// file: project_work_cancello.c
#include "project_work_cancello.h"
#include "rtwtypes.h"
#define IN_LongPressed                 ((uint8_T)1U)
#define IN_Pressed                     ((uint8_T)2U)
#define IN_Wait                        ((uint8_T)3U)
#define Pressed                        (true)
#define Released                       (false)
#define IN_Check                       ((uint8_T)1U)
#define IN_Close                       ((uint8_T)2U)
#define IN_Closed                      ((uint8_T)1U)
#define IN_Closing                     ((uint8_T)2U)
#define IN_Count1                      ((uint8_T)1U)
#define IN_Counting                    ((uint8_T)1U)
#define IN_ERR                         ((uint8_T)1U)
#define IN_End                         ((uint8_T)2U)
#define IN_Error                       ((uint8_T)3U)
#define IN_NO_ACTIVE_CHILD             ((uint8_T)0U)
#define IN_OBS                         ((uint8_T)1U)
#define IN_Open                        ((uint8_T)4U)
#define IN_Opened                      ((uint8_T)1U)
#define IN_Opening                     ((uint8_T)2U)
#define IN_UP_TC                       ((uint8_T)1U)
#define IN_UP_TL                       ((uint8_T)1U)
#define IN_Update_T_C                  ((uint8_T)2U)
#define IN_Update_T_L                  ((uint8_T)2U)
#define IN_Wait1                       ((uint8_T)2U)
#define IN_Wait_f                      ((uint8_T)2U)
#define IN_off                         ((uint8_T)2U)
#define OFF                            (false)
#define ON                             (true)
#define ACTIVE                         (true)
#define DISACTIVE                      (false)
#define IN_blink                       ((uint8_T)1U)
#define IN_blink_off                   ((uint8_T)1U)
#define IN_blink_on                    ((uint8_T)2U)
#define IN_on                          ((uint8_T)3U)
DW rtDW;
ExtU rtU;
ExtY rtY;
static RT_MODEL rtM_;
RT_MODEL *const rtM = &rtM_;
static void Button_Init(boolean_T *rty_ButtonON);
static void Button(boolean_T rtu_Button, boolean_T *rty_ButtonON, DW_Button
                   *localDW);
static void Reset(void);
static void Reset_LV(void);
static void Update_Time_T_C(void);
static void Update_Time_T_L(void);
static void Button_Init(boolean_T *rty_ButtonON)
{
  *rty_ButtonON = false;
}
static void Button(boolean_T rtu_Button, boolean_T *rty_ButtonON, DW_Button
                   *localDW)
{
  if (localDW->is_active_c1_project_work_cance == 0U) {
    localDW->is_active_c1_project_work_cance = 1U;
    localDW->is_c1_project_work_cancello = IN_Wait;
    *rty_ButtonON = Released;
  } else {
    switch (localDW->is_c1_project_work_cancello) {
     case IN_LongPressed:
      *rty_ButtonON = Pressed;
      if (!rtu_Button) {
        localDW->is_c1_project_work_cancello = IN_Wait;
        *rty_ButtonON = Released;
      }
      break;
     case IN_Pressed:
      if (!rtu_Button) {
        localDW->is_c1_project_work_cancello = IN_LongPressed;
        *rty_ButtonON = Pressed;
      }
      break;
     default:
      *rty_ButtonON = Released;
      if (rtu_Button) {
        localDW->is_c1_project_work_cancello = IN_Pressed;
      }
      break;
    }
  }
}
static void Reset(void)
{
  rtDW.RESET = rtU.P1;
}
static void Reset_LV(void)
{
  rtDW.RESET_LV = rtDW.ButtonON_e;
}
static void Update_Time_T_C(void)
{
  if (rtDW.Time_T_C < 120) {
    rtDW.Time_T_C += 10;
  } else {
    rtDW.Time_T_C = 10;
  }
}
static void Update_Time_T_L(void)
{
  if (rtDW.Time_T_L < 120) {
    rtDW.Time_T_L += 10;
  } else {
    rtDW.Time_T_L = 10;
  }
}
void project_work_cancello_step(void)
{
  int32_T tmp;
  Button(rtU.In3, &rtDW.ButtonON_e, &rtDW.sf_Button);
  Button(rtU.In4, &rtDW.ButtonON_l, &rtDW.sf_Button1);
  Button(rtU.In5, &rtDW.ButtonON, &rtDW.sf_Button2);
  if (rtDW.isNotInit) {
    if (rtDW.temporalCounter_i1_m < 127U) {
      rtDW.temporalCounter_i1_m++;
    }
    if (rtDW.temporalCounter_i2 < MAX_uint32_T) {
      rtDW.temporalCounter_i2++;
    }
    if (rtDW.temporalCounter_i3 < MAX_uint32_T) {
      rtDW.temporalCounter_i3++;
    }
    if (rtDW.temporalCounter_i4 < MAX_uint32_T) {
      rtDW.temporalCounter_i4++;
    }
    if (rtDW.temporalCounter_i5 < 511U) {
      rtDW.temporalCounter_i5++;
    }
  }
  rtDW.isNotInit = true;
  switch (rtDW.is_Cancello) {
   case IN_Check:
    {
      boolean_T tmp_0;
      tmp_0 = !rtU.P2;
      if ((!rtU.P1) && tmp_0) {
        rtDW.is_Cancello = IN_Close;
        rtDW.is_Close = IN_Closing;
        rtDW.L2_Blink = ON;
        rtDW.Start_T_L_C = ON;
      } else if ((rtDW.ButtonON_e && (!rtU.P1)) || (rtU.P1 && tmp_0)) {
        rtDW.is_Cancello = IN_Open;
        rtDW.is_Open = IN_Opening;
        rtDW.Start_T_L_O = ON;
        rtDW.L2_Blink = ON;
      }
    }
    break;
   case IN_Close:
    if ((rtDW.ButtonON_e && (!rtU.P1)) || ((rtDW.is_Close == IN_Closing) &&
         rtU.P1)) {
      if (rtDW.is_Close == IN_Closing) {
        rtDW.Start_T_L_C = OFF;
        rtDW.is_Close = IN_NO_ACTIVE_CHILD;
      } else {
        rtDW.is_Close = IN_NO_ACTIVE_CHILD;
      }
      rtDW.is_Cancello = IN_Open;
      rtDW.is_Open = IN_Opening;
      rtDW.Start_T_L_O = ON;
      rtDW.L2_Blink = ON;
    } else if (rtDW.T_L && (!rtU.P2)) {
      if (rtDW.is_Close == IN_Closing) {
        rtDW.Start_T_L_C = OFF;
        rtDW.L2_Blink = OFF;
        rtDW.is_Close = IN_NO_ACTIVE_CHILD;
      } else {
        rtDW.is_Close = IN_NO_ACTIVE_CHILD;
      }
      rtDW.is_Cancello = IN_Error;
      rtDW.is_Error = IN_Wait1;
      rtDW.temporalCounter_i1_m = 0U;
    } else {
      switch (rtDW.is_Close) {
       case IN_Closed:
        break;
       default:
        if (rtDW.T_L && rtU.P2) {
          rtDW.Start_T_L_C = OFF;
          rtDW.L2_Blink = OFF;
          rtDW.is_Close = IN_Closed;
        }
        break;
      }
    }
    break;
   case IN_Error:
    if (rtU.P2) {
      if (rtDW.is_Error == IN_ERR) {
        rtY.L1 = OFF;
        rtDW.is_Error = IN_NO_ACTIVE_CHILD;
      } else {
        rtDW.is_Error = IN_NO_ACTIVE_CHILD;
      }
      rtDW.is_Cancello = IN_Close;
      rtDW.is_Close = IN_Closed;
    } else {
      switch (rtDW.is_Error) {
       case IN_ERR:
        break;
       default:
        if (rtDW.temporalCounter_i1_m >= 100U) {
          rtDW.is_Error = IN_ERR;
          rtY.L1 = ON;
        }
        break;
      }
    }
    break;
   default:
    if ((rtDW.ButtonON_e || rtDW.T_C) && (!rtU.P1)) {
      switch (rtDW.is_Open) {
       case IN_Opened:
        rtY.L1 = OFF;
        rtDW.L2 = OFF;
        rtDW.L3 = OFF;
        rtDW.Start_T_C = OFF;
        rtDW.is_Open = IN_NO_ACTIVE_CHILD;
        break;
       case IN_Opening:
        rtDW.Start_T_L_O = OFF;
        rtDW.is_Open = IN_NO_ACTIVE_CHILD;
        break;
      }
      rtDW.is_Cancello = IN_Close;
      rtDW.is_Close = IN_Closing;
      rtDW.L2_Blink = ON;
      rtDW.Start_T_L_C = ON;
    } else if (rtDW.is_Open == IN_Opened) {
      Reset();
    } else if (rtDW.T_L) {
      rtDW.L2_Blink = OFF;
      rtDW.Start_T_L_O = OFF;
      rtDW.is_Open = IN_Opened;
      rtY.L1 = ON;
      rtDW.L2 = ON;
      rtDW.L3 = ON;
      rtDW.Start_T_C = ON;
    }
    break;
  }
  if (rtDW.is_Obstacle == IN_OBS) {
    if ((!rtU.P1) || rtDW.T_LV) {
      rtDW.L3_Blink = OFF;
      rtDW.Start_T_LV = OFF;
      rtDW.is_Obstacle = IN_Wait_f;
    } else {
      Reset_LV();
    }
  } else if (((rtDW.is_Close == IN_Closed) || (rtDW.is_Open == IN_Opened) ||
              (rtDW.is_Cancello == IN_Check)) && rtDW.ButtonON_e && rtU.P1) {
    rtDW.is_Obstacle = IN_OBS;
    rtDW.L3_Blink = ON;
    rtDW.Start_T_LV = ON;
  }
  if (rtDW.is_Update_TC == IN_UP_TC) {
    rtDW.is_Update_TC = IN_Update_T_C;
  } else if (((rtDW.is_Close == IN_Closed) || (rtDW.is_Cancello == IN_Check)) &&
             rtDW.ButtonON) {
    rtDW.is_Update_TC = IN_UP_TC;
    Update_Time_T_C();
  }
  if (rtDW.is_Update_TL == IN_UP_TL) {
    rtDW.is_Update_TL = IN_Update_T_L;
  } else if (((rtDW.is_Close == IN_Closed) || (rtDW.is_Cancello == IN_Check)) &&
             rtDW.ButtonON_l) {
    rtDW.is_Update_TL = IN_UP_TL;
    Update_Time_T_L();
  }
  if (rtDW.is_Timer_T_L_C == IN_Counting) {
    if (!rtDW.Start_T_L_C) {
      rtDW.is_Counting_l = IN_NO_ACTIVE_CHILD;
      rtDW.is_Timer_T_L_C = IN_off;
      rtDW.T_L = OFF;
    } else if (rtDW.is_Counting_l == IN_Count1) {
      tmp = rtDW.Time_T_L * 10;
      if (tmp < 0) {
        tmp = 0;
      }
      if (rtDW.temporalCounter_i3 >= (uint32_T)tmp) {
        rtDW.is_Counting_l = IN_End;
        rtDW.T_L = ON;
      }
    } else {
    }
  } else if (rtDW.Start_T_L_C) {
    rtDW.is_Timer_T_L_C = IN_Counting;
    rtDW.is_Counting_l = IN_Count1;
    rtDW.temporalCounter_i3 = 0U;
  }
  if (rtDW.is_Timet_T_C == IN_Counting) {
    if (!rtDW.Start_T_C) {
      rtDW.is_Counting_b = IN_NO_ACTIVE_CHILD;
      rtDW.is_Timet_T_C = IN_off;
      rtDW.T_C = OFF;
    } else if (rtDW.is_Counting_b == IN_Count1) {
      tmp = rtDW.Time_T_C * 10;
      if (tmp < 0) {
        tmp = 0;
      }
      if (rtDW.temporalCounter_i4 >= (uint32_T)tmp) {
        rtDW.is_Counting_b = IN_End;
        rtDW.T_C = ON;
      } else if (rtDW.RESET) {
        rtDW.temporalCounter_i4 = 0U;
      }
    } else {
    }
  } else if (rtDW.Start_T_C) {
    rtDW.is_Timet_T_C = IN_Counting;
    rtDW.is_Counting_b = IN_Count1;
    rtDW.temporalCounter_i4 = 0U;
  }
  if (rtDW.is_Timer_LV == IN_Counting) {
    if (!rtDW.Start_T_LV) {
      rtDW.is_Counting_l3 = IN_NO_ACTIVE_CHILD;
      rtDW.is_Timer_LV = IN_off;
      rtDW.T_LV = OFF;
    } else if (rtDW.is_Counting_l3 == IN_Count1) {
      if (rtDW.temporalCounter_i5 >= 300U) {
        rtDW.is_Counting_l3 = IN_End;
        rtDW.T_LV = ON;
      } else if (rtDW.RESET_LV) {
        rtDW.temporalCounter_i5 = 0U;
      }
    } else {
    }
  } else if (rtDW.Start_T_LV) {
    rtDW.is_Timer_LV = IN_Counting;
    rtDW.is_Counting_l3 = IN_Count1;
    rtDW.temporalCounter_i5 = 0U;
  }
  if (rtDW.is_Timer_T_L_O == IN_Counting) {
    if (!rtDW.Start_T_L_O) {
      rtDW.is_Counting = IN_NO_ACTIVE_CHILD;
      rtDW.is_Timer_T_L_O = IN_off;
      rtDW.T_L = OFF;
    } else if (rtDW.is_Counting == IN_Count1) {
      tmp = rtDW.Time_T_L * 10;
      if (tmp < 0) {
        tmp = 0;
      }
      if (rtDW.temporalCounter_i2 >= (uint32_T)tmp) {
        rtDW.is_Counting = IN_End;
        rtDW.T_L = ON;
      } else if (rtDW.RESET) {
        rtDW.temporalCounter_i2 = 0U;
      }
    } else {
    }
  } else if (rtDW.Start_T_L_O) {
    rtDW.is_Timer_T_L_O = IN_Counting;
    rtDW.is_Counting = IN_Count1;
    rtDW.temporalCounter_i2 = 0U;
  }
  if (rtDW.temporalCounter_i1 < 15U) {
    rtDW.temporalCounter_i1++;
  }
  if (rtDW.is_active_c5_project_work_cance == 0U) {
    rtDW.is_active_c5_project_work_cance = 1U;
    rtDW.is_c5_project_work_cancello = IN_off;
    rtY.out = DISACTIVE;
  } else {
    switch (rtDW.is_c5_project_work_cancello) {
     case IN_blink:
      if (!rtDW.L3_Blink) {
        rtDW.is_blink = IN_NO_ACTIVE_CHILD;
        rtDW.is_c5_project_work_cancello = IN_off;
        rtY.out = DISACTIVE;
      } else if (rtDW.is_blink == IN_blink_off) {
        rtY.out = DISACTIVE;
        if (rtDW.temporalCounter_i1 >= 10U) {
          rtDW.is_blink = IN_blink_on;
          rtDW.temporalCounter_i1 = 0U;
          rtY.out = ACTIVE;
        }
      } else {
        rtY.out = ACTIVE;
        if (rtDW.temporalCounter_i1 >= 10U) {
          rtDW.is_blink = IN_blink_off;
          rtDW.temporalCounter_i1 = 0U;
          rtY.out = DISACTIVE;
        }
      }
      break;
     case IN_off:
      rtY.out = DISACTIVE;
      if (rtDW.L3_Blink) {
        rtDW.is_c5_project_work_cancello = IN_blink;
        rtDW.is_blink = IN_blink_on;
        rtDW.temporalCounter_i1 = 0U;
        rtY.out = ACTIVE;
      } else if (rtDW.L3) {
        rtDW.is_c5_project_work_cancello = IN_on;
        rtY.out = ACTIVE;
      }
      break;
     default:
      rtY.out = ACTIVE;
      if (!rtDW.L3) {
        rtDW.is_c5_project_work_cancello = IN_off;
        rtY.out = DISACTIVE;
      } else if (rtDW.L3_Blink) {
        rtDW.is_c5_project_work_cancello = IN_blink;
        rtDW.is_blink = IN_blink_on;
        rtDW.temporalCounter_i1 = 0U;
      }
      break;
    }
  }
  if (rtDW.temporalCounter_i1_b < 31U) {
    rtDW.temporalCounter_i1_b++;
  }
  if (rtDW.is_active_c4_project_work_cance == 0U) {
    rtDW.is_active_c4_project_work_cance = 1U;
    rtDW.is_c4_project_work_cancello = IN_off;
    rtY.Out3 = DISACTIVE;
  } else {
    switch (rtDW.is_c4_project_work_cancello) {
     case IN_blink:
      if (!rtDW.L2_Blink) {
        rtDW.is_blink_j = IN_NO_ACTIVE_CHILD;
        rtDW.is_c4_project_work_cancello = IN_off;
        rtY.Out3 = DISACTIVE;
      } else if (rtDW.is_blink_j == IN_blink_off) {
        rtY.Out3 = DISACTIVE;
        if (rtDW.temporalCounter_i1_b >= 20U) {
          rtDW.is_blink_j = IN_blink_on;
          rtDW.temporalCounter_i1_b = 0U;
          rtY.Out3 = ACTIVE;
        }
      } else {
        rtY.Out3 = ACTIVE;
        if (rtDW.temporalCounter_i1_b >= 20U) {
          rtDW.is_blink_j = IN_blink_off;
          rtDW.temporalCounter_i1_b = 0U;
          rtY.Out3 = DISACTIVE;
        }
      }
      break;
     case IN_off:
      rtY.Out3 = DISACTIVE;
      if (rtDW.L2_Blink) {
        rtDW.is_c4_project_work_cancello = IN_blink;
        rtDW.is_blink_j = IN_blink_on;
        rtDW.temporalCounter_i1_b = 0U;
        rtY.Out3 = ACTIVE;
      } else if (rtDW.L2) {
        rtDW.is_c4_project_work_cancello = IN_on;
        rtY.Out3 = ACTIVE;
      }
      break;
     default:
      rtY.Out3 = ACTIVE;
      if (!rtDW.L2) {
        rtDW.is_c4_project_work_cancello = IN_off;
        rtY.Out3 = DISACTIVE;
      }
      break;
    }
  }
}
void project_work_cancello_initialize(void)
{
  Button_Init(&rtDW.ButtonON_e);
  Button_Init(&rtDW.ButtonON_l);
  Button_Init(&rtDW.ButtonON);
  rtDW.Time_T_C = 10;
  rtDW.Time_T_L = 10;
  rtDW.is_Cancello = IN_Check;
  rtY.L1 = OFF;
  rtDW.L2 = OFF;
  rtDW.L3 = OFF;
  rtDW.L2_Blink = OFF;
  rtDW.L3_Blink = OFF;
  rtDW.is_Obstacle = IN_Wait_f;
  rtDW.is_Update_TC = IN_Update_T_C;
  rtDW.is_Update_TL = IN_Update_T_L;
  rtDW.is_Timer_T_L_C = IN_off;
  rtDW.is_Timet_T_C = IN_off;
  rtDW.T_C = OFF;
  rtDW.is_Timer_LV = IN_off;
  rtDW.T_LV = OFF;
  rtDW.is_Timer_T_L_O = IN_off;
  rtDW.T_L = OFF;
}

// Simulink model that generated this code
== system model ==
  P1 : Inport
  P2 : Inport
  In3 : Inport
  In4 : Inport
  In5 : Inport
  L1 : Outport  <- 1: Cancello
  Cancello : Stateflow chart  <- 1: P1, 2: P2, 3: Button, 4: Button1, 5: Button2
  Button : Stateflow chart  <- 1: In3
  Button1 : Stateflow chart  <- 1: In4
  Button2 : Stateflow chart  <- 1: In5
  out : Outport  <- 1: Stateflowchart#1
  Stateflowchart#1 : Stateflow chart  <- 1: Cancello/5, 2: Cancello/3
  Out3 : Outport  <- 1: Stateflowchart#2
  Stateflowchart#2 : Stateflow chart  <- 1: Cancello/4, 2: Cancello/2
== stateflow chart Button ==
  state Wait
    en:ButtonON=Released
  state Pressed
  state LongPressed
    en: ButtonON=Pressed
  (default) -> Wait
  Wait -> Pressed : [Button==Pressed]
  LongPressed -> Wait : [Button==Released]
  Pressed -> LongPressed : [Button==Released]
  data: Button input boolean; ButtonON output boolean; Pressed constant boolean =true; Released constant boolean =false

== stateflow chart Button1 ==
  state Wait
    en:ButtonON=Released
  state Pressed
  state LongPressed
    en: ButtonON=Pressed
  (default) -> Wait
  Wait -> Pressed : [Button==Pressed]
  LongPressed -> Wait : [Button==Released]
  Pressed -> LongPressed : [Button==Released]
  data: Button input boolean; ButtonON output boolean; Pressed constant boolean =true; Released constant boolean =false

== stateflow chart Cancello ==
  state Cancello [parallel]
    settings: executionOrder=1
    state Check
      en: L1=OFF; L2=OFF; L3=OFF;L2_Blink=OFF;L3_Blink=OFF
    state Error
      state Wait1
      state ERR
        en: L1=ON
        ex: L1=OFF
      (default) -> Wait1
      Wait1 -> ERR : [after(10,sec)]
    state Close
      state Closing
        en:L2_Blink=ON; Start_T_L_C=ON;
        ex:Start_T_L_C=OFF; L2_Blink=OFF;
      state Closed
      (default) -> Closing
      Closing -> Closed : [T_L==ON && P2 == true]
    state Open
      state Opening
        en: Start_T_L_O=ON;L2_Blink=ON;
        ex:L2_Blink=OFF,Start_T_L_O=OFF
      state Opened
        en:L1=ON; L2=ON; L3=ON; Start_T_C=ON;
        du: Reset();
        ex: L1=OFF; L2=OFF; L3=OFF; Start_T_C=OFF;
      (default) -> Opening
      Opening -> Opened : [T_L == ON]
    (default) -> Check
    Check -> Open [order 2] : [B1 == ON && P1 == OFF || P1 == ON && P2 == OFF]
    Close -> Error [order 2] : [T_L==ON&&P2==false]
    Check -> Close [order 1] : [P1 == OFF && P2 == OFF]
    Close -> Open [order 1] : [B1 == ON && P1 == false || in(Close.Closing) && P1==true]
    Error -> Closed : [P2==true]
    Open -> Close : [(B1 == ON || T_C == true) && P1==false]
  state Timer_T_L_O [parallel]
    settings: executionOrder=7
    state Counting
      state Count1
      state End
        en: T_L = ON
      (default) -> Timer_T_L_O.Counting.Count1
      Timer_T_L_O.Counting.Count1 -> Timer_T_L_O.Counting.End [order 1] : [after(Time_T_L,sec)]
      Timer_T_L_O.Counting.Count1 -> Timer_T_L_O.Counting.Count1 [order 2] : [RESET == ON]
    state off
      en: T_L =OFF
    (default) -> Timer_T_L_O.off
    Timer_T_L_O.off -> Timer_T_L_O.Counting : [Start_T_L_O == ON]
    Timer_T_L_O.Counting -> Timer_T_L_O.off : [Start_T_L_O == OFF]
  state Timer_T_L_C [parallel]
    settings: executionOrder=4
    state Counting
      state Count1
      state End
        en: T_L = ON
      (default) -> Timer_T_L_C.Counting.Count1
      Timer_T_L_C.Counting.Count1 -> Timer_T_L_C.Counting.End : [after(Time_T_L,sec)]
    state off
      en: T_L =OFF
    (default) -> Timer_T_L_C.off
    Timer_T_L_C.off -> Timer_T_L_C.Counting : [Start_T_L_C == ON]
    Timer_T_L_C.Counting -> Timer_T_L_C.off : [Start_T_L_C == OFF]
  state Reset [function]
    (default) -> (junction 65)
    (junction 65) -> (junction 68) [order 1] : [P1==true]
    (junction 68) -> (junction 73) : {RESET=true;}
    (junction 65) -> (junction 71) [order 2] : [P1==false]
    (junction 71) -> (junction 73) : {RESET=false;}
  state Update_Time_T_L [function]
    (default) -> (junction 97)
    (junction 97) -> (junction 99) [order 1] : [Time_T_L < 120]
    (junction 99) -> (junction 107) : {Time_T_L=Time_T_L+10}
    (junction 97) -> (junction 103) [order 2] : [Time_T_L >= 120]
    (junction 103) -> (junction 107) : {Time_T_L = 10}
  state Timet_T_C [parallel]
    settings: executionOrder=5
    state Counting
      state Count1
      state End
        en: T_C = ON
      (default) -> Timet_T_C.Counting.Count1
      Timet_T_C.Counting.Count1 -> Timet_T_C.Counting.End [order 1] : [after(Time_T_C,sec)]
      Timet_T_C.Counting.Count1 -> Timet_T_C.Counting.Count1 [order 2] : [RESET == ON]
    state off
      en: T_C =OFF
    (default) -> Timet_T_C.off
    Timet_T_C.off -> Timet_T_C.Counting : [Start_T_C == ON]
    Timet_T_C.Counting -> Timet_T_C.off : [Start_T_C == OFF]
  state Update_Time_T_C [function]
    (default) -> (junction 114)
    (junction 114) -> (junction 116) [order 1] : [Time_T_C < 120]
    (junction 116) -> (junction 120) : {Time_T_C=Time_T_C + 10}
    (junction 114) -> (junction 118) [order 2] : [Time_T_C >= 120]
    (junction 118) -> (junction 120) : {Time_T_C = 10}
  state Obstacle [parallel]
    settings: executionOrder=2
    state Wait
    state OBS
      en: L3_Blink=ON;Start_T_LV=ON
      du: Reset_LV()
      ex:L3_Blink=OFF;Start_T_LV=OFF
    (default) -> Wait
    Wait -> OBS : [(in(Cancello.Close.Closed) || in(Cancello.Open.Opened) || in(Cancello.Check)) && B1==ON &&P1==true]
    OBS -> Wait : [P1==false || T_LV==ON ]
  state Update [parallel]
    settings: executionOrder=3
    state Update_TC [parallel]
      settings: executionOrder=1
      state Update_T_C
      state UP_TC
        en: Update_Time_T_C()
      (default) -> Update_T_C
      UP_TC -> Update_T_C
      Update_T_C -> UP_TC : [(in(Cancello.Close.Closed)||in(Cancello.Check)) && B3 == ON]
    state Update_TL [parallel]
      settings: executionOrder=2
      state Update_T_L
      state UP_TL
        en: Update_Time_T_L()
      (default) -> Update_T_L
      UP_TL -> Update_T_L
      Update_T_L -> UP_TL : [(in(Cancello.Close.Closed) || in(Cancello.Check)) && B2==ON]
  state Timer_LV [parallel]
    settings: executionOrder=6
    state Counting
      state Count1
      state End
        en: T_LV = ON
      (default) -> Timer_LV.Counting.Count1
      Timer_LV.Counting.Count1 -> Timer_LV.Counting.End [order 1] : [after(30,sec)]
      Timer_LV.Counting.Count1 -> Timer_LV.Counting.Count1 [order 2] : [RESET_LV==true]
    state off
      en: T_LV =OFF
    (default) -> Timer_LV.off
    Timer_LV.off -> Timer_LV.Counting : [Start_T_LV == ON]
    Timer_LV.Counting -> Timer_LV.off : [Start_T_LV == OFF]
  state Reset_LV [function]
    (default) -> (junction 81)
    (junction 81) -> (junction 83) [order 1] : [B1==ON]
    (junction 81) -> (junction 89) [order 2] : [B1==OFF]
    (junction 83) -> (junction 87) : {RESET_LV=true}
    (junction 89) -> (junction 87) : {RESET_LV=false}
  data: L1 output boolean; L2 output boolean; L3 output boolean; OFF constant boolean =false; P1 input boolean; P2 input boolean; ON constant boolean =true; B1 input boolean; Time_T_C local int32 =10; Time_T_L local int32 =10; L2_Blink output boolean; L3_Blink output boolean; B2 input boolean; B3 input boolean; RESET local boolean; Start_T_C local boolean; Start_T_L_O local boolean; T_L local boolean; T_C local boolean; T_LV local boolean; RESET_LV local boolean; Start_T_LV local boolean; Start_T_L_C local boolean

== stateflow chart Stateflowchart#2 ==
  state blink
    state blink_on
      en: out = ACTIVE
    state blink_off
      en: out = DISACTIVE
    (default) -> blink_on
    blink_off -> blink_on : after(period, msec)
    blink_on -> blink_off : after(period, msec)
  state off
    en: out = DISACTIVE;
  state on
    en: out=ACTIVE
  (default) -> off
  off -> blink [order 1] : [enable == ACTIVE]
  off -> on [order 2] : [On==ACTIVE]
  blink -> off : [enable == DISACTIVE]
  on -> off : [On==DISACTIVE]
  data: enable input boolean; out output boolean; ACTIVE constant boolean =true; DISACTIVE constant boolean =false; period constant double =2000; On input boolean

== stateflow chart Stateflowchart#1 ==
  state blink
    state blink_on
      en: out = ACTIVE
    state blink_off
      en: out = DISACTIVE
    (default) -> blink_on
    blink_off -> blink_on : after(period, msec)
    blink_on -> blink_off : after(period, msec)
  state off
    en: out = DISACTIVE;
  state on
    en:out = ACTIVE
  (default) -> off
  off -> blink [order 1] : [enable == ACTIVE]
  off -> on [order 2] : [On==ACTIVE]
  blink -> off [order 1] : [enable == DISACTIVE]
  on -> off [order 1] : [On == DISACTIVE]
  blink -> on [order 2] : [enable == DISACTIVE && On == ACTIVE]
  on -> blink [order 2] : [enable == ACTIVE]
  data: enable input boolean; out output boolean; ACTIVE constant boolean =true; DISACTIVE constant boolean =false; period constant double =1000; On input boolean

== stateflow chart Button2 ==
  state Wait
    en:ButtonON=Released
  state Pressed
  state LongPressed
    en: ButtonON=Pressed
  (default) -> Wait
  Wait -> Pressed : [Button==Pressed]
  LongPressed -> Wait : [Button==Released]
  Pressed -> LongPressed : [Button==Released]
  data: Button input boolean; ButtonON output boolean; Pressed constant boolean =true; Released constant boolean =false
